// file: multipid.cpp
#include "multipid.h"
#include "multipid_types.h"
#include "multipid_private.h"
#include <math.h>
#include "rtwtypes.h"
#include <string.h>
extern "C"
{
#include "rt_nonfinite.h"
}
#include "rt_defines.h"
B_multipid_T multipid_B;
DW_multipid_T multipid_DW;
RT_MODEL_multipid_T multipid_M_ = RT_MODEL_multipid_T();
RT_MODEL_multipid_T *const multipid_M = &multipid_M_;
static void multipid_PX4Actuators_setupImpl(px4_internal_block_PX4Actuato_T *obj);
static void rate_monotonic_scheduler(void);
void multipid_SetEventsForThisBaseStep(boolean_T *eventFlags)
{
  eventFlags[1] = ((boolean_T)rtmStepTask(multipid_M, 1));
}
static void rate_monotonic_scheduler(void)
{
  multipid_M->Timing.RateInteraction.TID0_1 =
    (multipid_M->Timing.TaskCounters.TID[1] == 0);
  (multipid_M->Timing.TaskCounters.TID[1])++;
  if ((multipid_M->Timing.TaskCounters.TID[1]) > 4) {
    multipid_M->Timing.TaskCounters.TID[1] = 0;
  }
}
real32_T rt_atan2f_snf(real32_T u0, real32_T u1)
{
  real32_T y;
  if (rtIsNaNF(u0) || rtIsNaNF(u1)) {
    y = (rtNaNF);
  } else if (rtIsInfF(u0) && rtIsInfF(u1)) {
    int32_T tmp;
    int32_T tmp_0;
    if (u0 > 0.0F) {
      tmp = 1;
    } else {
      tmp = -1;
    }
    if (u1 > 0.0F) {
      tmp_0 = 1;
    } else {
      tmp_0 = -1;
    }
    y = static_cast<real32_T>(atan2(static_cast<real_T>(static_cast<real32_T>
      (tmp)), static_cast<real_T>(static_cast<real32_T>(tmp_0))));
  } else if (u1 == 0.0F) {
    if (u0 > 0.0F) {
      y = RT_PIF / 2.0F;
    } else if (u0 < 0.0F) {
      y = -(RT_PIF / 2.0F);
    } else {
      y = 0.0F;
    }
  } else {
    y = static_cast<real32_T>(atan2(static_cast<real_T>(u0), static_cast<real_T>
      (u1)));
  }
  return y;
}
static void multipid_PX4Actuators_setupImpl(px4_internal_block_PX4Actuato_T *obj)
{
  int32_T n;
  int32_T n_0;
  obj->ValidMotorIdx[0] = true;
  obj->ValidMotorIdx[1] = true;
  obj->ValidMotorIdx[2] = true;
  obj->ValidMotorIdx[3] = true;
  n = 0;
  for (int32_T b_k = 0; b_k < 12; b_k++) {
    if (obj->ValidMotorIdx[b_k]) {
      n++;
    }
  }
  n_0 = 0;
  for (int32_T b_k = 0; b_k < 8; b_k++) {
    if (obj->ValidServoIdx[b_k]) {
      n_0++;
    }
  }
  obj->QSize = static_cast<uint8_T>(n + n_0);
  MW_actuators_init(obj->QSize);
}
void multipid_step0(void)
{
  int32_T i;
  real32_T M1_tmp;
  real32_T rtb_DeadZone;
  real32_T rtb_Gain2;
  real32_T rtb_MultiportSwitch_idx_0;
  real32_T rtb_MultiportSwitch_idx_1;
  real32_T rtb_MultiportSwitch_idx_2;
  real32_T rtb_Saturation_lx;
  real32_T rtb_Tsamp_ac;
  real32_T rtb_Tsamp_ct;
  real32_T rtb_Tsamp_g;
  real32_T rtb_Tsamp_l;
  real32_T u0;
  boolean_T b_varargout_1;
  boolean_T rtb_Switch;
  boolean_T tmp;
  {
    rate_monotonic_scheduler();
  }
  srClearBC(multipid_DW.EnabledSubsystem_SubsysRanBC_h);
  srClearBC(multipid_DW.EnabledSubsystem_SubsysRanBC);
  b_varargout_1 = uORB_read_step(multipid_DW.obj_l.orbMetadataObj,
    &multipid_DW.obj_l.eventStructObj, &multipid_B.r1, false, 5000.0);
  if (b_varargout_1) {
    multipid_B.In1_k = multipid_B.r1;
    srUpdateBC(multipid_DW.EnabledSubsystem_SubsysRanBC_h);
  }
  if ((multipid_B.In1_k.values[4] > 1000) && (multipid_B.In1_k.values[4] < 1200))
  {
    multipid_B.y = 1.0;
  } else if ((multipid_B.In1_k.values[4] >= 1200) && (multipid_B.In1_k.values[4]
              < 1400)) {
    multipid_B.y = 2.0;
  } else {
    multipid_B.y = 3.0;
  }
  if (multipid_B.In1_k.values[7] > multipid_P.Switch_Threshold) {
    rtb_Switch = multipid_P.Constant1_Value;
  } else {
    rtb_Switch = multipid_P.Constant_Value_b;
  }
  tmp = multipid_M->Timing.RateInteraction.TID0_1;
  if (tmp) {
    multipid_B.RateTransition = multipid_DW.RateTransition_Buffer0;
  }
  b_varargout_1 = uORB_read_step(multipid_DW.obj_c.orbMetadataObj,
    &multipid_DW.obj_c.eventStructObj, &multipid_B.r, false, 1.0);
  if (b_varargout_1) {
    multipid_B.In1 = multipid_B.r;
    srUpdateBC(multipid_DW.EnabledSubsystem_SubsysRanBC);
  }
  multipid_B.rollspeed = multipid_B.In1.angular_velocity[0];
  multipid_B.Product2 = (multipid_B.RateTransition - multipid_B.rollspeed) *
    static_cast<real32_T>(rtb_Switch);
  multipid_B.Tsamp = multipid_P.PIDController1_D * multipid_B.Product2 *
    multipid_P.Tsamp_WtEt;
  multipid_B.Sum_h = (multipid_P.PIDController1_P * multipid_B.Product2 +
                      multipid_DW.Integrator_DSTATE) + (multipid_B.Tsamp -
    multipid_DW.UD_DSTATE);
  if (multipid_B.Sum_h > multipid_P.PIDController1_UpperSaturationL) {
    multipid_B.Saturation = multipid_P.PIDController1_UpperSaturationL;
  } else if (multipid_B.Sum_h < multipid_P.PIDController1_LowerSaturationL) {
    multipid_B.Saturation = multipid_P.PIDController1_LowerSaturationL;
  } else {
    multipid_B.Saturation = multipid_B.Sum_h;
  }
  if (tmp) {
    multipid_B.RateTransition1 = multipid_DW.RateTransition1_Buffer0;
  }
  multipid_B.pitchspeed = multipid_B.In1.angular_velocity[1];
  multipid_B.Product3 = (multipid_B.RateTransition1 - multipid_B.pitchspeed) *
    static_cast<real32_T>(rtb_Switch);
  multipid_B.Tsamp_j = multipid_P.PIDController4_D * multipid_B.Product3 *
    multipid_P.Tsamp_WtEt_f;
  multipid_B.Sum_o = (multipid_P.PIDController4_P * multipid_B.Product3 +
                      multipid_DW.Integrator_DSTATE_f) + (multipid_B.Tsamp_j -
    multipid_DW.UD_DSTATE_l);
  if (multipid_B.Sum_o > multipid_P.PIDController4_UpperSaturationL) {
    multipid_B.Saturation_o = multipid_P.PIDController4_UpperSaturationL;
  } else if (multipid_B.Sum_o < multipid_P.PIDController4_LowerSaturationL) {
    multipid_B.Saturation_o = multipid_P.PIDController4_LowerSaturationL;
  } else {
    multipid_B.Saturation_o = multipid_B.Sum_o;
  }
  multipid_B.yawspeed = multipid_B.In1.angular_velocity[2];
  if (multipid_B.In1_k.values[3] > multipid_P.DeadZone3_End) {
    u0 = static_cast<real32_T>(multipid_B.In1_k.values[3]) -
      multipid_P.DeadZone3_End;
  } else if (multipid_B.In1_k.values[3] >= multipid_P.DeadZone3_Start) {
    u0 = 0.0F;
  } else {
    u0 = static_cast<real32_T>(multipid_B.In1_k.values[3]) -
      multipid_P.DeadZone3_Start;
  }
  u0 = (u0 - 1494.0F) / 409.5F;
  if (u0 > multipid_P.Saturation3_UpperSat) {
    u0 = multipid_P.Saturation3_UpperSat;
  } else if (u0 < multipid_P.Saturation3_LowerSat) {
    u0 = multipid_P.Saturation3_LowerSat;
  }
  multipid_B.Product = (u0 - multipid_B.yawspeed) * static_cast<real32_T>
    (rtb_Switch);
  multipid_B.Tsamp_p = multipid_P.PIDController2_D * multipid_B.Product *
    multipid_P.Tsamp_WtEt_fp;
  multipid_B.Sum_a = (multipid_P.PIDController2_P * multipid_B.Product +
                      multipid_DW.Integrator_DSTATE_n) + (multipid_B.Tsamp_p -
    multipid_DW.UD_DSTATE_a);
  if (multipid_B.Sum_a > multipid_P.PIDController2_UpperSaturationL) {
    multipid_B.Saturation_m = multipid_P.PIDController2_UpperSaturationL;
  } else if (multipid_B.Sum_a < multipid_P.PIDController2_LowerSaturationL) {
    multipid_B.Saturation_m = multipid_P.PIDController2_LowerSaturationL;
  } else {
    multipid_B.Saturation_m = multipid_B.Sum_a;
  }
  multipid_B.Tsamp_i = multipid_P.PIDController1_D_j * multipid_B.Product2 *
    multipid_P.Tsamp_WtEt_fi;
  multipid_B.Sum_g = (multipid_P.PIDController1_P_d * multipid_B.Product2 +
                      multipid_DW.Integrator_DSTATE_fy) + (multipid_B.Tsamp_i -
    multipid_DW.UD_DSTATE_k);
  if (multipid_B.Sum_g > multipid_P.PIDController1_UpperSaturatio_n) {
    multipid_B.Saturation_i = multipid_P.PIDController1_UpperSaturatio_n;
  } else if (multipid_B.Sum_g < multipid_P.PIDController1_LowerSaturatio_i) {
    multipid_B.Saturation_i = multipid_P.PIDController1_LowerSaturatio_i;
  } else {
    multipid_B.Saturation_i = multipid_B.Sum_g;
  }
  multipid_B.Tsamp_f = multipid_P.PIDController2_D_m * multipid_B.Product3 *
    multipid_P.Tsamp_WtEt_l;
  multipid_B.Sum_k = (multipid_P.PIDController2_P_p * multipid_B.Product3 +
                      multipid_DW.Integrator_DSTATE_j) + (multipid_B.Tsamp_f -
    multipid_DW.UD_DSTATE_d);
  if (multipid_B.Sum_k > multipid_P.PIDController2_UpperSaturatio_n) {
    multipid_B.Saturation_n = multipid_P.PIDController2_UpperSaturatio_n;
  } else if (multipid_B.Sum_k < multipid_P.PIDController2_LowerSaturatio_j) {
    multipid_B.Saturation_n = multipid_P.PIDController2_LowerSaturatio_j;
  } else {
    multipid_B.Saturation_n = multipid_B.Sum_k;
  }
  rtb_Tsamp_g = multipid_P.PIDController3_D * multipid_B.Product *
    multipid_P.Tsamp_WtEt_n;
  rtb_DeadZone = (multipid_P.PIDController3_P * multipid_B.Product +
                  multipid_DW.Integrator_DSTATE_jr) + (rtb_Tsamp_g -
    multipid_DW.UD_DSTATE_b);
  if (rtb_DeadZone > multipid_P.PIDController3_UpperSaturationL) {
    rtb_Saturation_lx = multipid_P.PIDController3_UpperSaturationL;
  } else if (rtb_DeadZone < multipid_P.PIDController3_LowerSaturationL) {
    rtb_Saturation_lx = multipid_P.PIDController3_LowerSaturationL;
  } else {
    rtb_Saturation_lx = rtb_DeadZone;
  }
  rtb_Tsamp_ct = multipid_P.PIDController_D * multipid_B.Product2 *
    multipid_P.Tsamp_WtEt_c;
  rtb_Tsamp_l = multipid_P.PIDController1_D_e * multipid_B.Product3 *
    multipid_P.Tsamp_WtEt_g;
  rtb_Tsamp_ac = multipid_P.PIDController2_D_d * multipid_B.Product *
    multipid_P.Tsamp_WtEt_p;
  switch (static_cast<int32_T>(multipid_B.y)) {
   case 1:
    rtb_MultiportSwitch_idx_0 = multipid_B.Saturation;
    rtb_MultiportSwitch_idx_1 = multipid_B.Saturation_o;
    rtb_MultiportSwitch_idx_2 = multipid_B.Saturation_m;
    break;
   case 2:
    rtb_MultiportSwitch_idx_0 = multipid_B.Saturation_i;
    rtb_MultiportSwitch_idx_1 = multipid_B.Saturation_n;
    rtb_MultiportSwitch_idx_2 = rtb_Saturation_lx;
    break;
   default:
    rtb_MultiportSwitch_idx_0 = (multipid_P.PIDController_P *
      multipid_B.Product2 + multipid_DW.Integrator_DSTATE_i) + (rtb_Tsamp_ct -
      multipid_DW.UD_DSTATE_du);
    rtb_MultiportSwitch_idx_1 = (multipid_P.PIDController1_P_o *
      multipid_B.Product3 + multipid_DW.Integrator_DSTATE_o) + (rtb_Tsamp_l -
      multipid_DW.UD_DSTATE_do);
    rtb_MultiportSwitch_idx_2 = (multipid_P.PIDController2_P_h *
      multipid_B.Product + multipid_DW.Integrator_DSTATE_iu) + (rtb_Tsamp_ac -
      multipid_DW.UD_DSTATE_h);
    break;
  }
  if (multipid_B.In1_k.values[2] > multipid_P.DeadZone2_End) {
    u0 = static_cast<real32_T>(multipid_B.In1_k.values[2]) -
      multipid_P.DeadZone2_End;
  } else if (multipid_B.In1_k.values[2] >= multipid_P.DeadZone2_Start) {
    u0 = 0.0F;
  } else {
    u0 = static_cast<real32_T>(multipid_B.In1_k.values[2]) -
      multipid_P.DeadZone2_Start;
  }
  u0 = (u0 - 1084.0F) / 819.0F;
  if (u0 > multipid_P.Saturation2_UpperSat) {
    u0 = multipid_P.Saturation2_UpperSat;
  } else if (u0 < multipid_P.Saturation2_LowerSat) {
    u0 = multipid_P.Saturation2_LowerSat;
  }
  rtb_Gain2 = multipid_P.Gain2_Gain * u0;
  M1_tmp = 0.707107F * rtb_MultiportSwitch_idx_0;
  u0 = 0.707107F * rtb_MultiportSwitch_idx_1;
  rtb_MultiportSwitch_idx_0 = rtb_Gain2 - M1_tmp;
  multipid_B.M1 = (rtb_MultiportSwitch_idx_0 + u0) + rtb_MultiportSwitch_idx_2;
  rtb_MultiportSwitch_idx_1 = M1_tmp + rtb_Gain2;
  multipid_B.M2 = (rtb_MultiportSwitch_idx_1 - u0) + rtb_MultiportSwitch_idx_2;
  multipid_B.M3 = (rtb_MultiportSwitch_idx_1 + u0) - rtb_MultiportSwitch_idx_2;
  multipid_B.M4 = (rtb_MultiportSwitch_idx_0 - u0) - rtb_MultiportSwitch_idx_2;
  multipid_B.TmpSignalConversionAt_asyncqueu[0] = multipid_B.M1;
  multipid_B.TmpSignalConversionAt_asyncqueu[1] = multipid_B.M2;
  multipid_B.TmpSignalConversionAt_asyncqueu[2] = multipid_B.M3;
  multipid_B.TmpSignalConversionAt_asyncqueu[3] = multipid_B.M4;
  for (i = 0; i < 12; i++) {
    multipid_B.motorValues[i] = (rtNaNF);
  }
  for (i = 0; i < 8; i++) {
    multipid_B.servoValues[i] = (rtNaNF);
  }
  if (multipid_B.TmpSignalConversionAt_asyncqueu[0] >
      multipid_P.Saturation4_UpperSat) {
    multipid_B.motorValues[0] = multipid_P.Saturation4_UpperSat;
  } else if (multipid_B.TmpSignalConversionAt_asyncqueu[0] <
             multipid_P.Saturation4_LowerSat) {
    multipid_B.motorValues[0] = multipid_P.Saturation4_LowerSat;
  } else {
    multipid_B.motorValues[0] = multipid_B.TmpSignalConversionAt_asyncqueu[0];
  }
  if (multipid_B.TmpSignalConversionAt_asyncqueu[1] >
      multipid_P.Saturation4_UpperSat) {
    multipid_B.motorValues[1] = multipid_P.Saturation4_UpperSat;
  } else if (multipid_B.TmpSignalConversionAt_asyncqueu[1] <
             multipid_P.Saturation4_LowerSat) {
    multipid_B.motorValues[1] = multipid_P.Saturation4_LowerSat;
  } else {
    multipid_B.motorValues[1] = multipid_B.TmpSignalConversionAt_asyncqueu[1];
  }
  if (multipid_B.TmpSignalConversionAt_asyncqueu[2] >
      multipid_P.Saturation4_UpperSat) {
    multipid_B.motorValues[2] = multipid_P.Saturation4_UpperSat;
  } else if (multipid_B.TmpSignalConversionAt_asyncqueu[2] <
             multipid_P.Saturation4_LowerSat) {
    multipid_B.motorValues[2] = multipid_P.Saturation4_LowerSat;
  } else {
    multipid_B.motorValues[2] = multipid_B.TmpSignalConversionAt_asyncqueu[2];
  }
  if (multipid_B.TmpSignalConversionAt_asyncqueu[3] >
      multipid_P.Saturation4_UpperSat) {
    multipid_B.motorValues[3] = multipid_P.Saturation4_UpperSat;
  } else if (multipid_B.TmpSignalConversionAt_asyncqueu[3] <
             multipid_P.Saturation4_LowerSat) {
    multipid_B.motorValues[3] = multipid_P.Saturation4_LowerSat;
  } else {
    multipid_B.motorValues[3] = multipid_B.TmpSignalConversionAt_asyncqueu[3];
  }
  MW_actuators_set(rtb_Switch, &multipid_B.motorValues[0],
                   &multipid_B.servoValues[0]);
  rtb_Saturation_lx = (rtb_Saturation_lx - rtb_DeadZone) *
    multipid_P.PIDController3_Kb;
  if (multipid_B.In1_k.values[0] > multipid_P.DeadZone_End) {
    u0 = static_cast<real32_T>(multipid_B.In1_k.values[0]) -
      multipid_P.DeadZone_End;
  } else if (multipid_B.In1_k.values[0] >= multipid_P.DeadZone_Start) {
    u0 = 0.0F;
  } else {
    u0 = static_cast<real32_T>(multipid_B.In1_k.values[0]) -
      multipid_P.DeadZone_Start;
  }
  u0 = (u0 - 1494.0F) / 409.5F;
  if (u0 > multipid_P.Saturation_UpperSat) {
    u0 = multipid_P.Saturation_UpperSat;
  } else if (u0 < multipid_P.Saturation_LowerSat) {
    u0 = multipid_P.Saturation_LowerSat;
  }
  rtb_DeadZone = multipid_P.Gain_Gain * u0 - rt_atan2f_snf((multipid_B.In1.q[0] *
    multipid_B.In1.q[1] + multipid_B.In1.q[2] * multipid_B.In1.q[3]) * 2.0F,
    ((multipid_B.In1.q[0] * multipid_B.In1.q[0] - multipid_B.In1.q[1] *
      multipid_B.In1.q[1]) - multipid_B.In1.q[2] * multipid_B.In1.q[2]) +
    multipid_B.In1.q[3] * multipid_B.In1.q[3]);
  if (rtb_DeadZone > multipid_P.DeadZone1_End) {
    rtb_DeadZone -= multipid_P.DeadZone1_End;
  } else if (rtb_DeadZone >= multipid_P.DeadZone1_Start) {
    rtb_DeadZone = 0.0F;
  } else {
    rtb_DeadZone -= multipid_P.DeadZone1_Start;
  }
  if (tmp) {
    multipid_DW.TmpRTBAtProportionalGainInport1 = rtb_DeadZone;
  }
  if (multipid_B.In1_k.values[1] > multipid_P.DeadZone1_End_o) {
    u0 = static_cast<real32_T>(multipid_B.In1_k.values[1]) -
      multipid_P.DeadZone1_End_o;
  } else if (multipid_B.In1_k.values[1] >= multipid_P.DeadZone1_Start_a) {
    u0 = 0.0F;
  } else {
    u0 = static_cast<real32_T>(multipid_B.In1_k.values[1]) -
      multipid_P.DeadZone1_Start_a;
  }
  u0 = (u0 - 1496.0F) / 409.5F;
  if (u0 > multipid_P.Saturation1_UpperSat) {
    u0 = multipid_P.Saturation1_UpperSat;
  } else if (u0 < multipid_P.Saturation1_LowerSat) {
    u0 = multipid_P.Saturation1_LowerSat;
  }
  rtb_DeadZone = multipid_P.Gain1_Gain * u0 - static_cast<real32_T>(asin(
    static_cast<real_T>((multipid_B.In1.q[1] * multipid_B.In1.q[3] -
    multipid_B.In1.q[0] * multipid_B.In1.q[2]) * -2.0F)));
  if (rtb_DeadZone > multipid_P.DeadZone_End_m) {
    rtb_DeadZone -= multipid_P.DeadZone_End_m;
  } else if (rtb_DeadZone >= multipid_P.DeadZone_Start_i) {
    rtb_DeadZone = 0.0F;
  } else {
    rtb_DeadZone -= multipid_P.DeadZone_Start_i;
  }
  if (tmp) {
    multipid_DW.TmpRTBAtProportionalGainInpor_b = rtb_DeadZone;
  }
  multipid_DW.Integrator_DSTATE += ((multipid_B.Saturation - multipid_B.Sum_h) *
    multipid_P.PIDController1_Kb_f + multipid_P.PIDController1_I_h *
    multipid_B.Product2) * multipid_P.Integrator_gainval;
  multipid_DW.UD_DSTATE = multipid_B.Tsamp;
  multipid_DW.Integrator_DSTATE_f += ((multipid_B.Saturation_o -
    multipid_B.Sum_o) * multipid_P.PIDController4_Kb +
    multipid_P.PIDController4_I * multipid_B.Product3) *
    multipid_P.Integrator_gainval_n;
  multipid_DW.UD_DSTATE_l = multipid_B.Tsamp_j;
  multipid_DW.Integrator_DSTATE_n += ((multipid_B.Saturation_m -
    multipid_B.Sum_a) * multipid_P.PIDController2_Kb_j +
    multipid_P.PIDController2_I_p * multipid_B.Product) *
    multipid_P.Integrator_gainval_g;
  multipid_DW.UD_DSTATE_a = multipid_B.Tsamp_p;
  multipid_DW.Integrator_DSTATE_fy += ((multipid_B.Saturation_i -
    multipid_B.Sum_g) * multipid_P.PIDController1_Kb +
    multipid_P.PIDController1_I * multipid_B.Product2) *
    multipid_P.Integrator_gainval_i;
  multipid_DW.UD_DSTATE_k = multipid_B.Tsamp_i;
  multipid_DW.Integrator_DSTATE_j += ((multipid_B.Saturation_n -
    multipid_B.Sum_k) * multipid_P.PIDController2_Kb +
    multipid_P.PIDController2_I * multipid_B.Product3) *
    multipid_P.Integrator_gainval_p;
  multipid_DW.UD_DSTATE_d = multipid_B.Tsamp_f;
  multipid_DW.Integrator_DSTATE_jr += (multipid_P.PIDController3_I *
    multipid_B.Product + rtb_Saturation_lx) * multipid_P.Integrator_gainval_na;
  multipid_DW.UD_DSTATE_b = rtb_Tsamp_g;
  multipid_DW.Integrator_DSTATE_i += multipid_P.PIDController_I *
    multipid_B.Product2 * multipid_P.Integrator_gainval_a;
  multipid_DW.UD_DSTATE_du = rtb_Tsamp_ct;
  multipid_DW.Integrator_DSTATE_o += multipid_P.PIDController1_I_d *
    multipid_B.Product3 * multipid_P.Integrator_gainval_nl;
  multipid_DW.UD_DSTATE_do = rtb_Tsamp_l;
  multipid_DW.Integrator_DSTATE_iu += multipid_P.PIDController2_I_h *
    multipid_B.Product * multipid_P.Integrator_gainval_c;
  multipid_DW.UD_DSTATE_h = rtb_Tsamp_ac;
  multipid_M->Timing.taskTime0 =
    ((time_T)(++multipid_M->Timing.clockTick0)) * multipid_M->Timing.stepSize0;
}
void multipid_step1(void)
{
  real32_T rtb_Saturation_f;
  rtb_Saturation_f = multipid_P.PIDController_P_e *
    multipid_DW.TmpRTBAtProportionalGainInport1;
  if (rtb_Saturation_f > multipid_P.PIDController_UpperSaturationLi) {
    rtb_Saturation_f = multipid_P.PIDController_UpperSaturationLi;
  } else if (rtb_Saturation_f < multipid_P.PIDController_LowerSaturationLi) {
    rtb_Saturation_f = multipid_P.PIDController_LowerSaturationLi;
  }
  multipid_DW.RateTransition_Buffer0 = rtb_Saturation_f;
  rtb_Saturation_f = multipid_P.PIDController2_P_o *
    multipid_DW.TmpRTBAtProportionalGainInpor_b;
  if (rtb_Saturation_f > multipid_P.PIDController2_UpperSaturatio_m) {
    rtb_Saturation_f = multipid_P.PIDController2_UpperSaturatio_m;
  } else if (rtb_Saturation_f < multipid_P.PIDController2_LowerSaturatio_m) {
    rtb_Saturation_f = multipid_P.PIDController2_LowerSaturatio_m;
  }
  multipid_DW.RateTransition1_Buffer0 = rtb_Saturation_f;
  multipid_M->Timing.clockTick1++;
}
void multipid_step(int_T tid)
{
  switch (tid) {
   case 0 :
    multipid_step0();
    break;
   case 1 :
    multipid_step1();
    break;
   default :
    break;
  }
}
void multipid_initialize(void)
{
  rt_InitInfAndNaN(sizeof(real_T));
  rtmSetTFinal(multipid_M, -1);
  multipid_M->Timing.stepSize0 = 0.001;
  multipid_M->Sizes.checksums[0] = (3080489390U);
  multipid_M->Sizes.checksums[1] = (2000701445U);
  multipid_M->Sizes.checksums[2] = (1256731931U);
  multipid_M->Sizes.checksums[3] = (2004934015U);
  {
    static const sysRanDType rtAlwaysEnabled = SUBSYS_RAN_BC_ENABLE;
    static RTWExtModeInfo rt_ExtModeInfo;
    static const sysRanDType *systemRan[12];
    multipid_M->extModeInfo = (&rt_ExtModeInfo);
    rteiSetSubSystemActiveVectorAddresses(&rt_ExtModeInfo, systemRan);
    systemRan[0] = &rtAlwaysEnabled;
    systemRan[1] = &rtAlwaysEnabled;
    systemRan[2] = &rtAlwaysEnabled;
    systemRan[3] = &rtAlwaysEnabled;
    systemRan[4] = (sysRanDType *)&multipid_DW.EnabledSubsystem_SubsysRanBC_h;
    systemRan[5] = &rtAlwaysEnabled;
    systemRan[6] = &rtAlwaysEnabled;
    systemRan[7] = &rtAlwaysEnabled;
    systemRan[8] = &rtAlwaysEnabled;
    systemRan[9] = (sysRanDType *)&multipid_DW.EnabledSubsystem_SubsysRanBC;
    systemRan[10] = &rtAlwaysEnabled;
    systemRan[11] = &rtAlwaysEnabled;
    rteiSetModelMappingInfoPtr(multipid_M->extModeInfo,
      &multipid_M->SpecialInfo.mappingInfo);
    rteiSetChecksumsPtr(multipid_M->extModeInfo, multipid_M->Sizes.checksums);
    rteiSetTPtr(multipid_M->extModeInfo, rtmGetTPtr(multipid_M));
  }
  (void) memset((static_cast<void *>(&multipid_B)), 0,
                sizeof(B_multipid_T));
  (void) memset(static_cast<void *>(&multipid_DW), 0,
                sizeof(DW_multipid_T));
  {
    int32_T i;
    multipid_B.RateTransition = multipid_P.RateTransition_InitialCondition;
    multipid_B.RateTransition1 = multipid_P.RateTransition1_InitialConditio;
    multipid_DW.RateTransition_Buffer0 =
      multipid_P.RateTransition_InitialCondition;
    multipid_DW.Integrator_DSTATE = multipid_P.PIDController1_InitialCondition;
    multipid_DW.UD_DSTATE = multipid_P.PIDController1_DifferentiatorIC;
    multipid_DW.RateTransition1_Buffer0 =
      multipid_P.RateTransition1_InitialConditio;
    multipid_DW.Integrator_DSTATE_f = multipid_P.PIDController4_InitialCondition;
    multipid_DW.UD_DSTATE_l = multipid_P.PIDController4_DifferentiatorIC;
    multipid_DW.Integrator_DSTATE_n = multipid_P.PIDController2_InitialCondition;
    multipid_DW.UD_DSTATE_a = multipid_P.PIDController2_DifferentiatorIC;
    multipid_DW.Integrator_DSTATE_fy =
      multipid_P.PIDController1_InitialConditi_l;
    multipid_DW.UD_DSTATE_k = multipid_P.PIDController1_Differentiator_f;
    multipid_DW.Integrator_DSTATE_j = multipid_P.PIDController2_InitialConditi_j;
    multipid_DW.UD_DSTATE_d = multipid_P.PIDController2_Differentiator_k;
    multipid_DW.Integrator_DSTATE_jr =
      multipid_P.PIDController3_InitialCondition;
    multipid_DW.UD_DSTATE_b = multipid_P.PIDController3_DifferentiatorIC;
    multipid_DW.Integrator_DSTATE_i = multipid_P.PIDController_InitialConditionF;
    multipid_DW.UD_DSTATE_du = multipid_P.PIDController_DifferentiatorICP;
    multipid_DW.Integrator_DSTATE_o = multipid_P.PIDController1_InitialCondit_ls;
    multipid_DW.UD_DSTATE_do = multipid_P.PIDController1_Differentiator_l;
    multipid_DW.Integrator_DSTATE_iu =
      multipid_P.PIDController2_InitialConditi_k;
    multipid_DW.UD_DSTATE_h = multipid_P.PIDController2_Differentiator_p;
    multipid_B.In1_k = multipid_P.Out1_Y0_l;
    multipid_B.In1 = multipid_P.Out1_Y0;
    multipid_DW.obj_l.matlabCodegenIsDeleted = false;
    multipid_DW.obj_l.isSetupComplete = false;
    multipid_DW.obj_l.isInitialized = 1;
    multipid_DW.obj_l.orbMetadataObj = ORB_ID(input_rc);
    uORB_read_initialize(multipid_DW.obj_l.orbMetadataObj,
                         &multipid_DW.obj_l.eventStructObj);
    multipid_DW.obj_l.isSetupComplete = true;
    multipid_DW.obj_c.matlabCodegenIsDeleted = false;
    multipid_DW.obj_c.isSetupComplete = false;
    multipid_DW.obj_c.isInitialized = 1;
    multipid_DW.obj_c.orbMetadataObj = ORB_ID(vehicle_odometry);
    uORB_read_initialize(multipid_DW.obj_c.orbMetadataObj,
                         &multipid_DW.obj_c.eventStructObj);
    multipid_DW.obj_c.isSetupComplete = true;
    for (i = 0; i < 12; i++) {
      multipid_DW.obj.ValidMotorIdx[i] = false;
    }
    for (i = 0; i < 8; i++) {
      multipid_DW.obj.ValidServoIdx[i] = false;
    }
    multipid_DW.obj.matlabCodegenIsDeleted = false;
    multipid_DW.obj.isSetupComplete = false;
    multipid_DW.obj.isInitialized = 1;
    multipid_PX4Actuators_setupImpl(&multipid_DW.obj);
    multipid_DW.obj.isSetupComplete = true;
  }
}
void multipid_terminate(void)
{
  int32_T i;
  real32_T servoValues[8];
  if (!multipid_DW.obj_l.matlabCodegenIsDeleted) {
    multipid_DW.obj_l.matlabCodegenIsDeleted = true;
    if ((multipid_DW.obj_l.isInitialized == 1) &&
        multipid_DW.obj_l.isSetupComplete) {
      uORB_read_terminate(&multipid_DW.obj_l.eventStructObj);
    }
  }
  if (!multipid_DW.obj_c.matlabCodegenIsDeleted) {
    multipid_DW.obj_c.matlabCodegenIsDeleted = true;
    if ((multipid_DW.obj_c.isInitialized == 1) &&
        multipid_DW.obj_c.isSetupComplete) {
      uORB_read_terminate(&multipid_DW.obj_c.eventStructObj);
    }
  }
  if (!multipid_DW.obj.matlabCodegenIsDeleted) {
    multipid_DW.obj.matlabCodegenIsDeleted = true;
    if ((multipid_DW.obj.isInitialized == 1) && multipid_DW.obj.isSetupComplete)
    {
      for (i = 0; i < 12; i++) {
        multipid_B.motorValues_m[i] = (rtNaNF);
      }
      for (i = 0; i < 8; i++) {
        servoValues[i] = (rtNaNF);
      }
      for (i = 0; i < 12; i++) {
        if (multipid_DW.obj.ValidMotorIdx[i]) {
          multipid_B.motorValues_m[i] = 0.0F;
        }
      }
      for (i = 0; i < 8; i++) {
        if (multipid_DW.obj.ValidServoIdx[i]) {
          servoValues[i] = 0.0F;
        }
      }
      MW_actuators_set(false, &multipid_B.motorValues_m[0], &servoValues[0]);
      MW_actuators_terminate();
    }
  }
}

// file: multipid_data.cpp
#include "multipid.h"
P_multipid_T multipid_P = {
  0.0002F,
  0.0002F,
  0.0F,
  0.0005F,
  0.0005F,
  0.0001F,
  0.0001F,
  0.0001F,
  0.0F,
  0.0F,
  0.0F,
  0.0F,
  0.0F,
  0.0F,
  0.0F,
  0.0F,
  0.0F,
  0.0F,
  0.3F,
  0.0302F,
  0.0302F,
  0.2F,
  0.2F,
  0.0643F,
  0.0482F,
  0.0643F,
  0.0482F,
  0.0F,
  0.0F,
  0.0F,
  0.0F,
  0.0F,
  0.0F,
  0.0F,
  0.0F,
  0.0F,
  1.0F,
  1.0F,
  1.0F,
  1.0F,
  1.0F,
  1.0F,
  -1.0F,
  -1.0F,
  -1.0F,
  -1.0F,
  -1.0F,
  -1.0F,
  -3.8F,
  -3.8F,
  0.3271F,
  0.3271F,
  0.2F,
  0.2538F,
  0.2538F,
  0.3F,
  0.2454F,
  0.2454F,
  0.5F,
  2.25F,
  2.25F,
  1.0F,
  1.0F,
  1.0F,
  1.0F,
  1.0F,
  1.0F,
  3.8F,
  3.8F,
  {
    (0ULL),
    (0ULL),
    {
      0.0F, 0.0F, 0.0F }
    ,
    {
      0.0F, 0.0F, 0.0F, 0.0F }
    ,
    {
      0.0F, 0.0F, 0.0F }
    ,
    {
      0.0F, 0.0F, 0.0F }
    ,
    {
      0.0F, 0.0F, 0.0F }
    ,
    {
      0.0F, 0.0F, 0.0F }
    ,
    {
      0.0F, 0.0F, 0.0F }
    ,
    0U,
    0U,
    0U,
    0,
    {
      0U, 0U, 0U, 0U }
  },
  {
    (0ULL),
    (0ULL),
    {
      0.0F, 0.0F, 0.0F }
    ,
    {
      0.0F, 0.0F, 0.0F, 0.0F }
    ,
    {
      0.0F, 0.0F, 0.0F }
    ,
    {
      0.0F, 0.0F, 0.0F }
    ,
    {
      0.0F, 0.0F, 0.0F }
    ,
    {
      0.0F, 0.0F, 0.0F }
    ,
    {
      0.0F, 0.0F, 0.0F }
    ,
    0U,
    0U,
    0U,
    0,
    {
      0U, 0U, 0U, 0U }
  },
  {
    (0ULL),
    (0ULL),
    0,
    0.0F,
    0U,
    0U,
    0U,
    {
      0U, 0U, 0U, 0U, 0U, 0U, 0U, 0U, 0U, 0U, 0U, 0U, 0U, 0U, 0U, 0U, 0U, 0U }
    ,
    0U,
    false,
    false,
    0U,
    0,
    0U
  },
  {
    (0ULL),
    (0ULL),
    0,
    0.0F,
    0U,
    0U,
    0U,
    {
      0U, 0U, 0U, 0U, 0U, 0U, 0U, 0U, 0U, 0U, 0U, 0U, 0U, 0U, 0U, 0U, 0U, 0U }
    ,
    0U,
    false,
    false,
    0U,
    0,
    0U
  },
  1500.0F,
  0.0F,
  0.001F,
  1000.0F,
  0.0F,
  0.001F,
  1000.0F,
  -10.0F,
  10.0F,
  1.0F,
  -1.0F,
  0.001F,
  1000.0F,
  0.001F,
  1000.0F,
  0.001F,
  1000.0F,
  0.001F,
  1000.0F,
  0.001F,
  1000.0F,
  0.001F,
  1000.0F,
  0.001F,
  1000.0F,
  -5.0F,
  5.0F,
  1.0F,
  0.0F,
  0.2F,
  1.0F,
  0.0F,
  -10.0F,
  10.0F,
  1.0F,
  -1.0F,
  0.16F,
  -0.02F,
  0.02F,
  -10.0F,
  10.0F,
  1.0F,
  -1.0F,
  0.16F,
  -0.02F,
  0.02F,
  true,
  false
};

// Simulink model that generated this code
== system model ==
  PX4ActuatorWrite#1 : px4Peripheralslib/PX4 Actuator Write  <- 1: Switch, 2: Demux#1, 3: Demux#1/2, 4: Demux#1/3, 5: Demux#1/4
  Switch : Switch  Criteria=u2 > Threshold  Threshold=1500  <- 1: Constant1, 2: DataTypeConversion#1, 3: Constant
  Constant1 : Constant
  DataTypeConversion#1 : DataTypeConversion  <- 1: RadioControlTransmitter#1/7
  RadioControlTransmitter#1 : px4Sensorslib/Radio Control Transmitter
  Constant : Constant  Value=0
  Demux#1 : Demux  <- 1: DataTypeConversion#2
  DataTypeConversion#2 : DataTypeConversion  <- 1: Saturation4
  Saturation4 : Saturate  UpperLimit=1  LowerLimit=0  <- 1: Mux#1
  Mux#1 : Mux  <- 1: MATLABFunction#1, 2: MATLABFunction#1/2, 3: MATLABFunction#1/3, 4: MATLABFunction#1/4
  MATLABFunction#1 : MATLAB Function  <- 1: Gain2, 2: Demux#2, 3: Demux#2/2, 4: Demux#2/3
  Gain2 : Gain  Gain=0.2  <- 1: Saturation2
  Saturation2 : Saturate  UpperLimit=1  LowerLimit=0  <- 1: Fcn#1
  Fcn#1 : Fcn  Expr=(u - 1084) / 819  <- 1: DeadZone2
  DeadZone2 : DeadZone  LowerValue=-5  UpperValue=5  <- 1: DataTypeConversion#3
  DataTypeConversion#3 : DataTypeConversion  <- 1: RadioControlTransmitter#1/4
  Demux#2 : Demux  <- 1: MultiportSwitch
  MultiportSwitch : MultiPortSwitch  <- 1: MATLABFunction#2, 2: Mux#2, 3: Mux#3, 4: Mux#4
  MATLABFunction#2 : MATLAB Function  <- 1: RadioControlTransmitter#1/6
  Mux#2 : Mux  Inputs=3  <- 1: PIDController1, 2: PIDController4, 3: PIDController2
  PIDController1 : slpidlib/PID Controller  Controller=PID  Form=Parallel  TimeDomain=Discrete-time  IntegratorMethod=Forward Euler  P=0.3271  I=0.0643  D=0.0002  N=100  InitialConditionForIntegrator=0  ExternalReset=none  LimitOutput=on  UpperSaturationLimit=1  LowerSaturationLimit=-1  <- 1: Product2
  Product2 : Product  <- 1: Sum#1, 2: Switch
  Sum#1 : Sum  Inputs=+-  <- 1: RateTransition, 2: VehicleAttitude#1/2
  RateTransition : RateTransition  <- 1: PIDController
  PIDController : slpidlib/PID Controller  Controller=P  Form=Parallel  TimeDomain=Discrete-time  IntegratorMethod=Forward Euler  P=2.25  I=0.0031  D=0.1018  N=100  InitialConditionForIntegrator=0  ExternalReset=none  LimitOutput=on  UpperSaturationLimit=3.8  LowerSaturationLimit=-3.8  <- 1: DeadZone1
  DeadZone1 : DeadZone  LowerValue=-0.02  UpperValue=0.02  <- 1: Sum
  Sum : Sum  Inputs=+-  <- 1: Gain, 2: MATLABFunction#3
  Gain : Gain  Gain=0.16  <- 1: DataTypeConversion#4
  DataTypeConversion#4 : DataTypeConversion  <- 1: Saturation
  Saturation : Saturate  UpperLimit=1  LowerLimit=-1  <- 1: Fcn#2
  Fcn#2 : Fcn  Expr=(u - 1494) / 409.5  <- 1: DeadZone
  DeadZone : DeadZone  LowerValue=-10  UpperValue=10  <- 1: DataTypeConversion#5
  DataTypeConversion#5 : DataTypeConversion  <- 1: RadioControlTransmitter#1/2
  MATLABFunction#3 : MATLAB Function  <- 1: VehicleAttitude#1/5
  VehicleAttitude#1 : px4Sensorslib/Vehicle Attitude
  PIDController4 : slpidlib/PID Controller  Controller=PID  Form=Parallel  TimeDomain=Discrete-time  IntegratorMethod=Forward Euler  P=0.3271  I=0.0643  D=0.0002  N=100  InitialConditionForIntegrator=0  ExternalReset=none  LimitOutput=on  UpperSaturationLimit=1  LowerSaturationLimit=-1  <- 1: Product3
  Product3 : Product  <- 1: Sum#2, 2: Switch
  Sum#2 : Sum  Inputs=+-  <- 1: RateTransition1, 2: VehicleAttitude#1/3
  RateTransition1 : RateTransition  <- 1: PIDController#1
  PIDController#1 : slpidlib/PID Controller  Controller=P  Form=Parallel  TimeDomain=Discrete-time  IntegratorMethod=Forward Euler  P=2.25  I=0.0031  D=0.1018  N=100  InitialConditionForIntegrator=0  ExternalReset=none  LimitOutput=on  UpperSaturationLimit=3.8  LowerSaturationLimit=-3.8  <- 1: DeadZone#1
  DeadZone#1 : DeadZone  LowerValue=-0.02  UpperValue=0.02  <- 1: Sum#3
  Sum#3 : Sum  Inputs=+-  <- 1: Gain1, 2: MATLABFunction#3/2
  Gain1 : Gain  Gain=0.16  <- 1: DataTypeConversion#6
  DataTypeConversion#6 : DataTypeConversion  <- 1: Saturation1
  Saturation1 : Saturate  UpperLimit=1  LowerLimit=-1  <- 1: Fcn#3
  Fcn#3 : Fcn  Expr=(u - 1496) / 409.5  <- 1: DeadZone#2
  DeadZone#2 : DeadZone  LowerValue=-10  UpperValue=10  <- 1: DataTypeConversion#7
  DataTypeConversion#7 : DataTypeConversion  <- 1: RadioControlTransmitter#1/3
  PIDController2 : slpidlib/PID Controller  Controller=PID  Form=Parallel  TimeDomain=Discrete-time  IntegratorMethod=Forward Euler  P=0.2  I=0.2  D=0  N=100  InitialConditionForIntegrator=0  ExternalReset=none  LimitOutput=on  UpperSaturationLimit=1  LowerSaturationLimit=-1  <- 1: Product
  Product : Product  <- 1: Sum#4, 2: Switch
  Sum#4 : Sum  Inputs=+-  <- 1: From#1, 2: VehicleAttitude#1/4
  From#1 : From
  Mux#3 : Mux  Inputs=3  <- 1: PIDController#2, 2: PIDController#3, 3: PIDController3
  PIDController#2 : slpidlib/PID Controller  Controller=PID  Form=Parallel  TimeDomain=Discrete-time  IntegratorMethod=Forward Euler  P=0.2538  I=0.0302  D=0.0005  N=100  InitialConditionForIntegrator=0  ExternalReset=none  LimitOutput=on  UpperSaturationLimit=1  LowerSaturationLimit=-1  <- 1: Product2
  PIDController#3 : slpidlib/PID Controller  Controller=PID  Form=Parallel  TimeDomain=Discrete-time  IntegratorMethod=Forward Euler  P=0.2538  I=0.0302  D=0.0005  N=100  InitialConditionForIntegrator=0  ExternalReset=none  LimitOutput=on  UpperSaturationLimit=1  LowerSaturationLimit=-1  <- 1: Product3
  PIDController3 : slpidlib/PID Controller  Controller=PID  Form=Parallel  TimeDomain=Discrete-time  IntegratorMethod=Forward Euler  P=0.3  I=0.3  D=0.0001  N=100  InitialConditionForIntegrator=0  ExternalReset=none  LimitOutput=on  UpperSaturationLimit=1  LowerSaturationLimit=-1  <- 1: Product
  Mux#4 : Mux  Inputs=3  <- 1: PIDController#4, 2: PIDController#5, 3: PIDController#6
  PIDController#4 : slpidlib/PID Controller  Controller=PID  Form=Parallel  TimeDomain=Discrete-time  IntegratorMethod=Forward Euler  P=0.2454  I=0.0482  D=0.0001  N=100  InitialConditionForIntegrator=0  ExternalReset=none  LimitOutput=off  UpperSaturationLimit=inf  LowerSaturationLimit=-inf  <- 1: Product2
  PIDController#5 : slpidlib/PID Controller  Controller=PID  Form=Parallel  TimeDomain=Discrete-time  IntegratorMethod=Forward Euler  P=0.2454  I=0.0482  D=0.0001  N=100  InitialConditionForIntegrator=0  ExternalReset=none  LimitOutput=off  UpperSaturationLimit=inf  LowerSaturationLimit=-inf  <- 1: Product3
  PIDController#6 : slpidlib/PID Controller  Controller=PID  Form=Parallel  TimeDomain=Discrete-time  IntegratorMethod=Forward Euler  P=0.5  I=0.2  D=0  N=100  InitialConditionForIntegrator=0  ExternalReset=none  LimitOutput=off  UpperSaturationLimit=inf  LowerSaturationLimit=-inf  <- 1: Product
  Goto#1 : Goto  <- 1: Saturation3
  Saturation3 : Saturate  UpperLimit=1  LowerLimit=-1  <- 1: Fcn#4
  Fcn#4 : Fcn  Expr=(u - 1494) / 409.5  <- 1: DeadZone3
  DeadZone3 : DeadZone  LowerValue=-10  UpperValue=10  <- 1: DataTypeConversion#8
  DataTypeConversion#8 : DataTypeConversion  <- 1: RadioControlTransmitter#1/5
== matlab function MATLABFunction#2 ==
function y = fcn(u)
%#codegen
y=0;
if u>1000 && u<1200 
   y=1;
elseif    u >= 1200 && u<1400
    y=2;
else
    y=3;
end

== matlab function MATLABFunction#1 ==
function [M1,M2,M3,M4]  = fcn(t,r, p, y)
M1 = t - 0.707107*r + 0.707107*p + y;
M2 = t + 0.707107*r - 0.707107*p + y;
M3 = t + 0.707107*r + 0.707107*p - y;
M4 = t - 0.707107*r - 0.707107*p - y;

== matlab function MATLABFunction#3 ==
function [phi,theta,psi] = quat2eul(q)

% Quaternion conversion to Euler angles based on the PX4 Firmware v1.10.2
% release.

phi = atan2(2*(q(1)*q(2) + q(3)* q(4)), q(1)^2 - q(2)^2 - q(3)^2 + q(4)^2);
theta = asin(-2*(q(2)*q(4) - q(1)*q(3)));
psi = atan2(2*(q(2)*q(3) + q(1)* q(4)), q(1)^2 + q(2)^2 - q(3)^2 - q(4)^2);
end
